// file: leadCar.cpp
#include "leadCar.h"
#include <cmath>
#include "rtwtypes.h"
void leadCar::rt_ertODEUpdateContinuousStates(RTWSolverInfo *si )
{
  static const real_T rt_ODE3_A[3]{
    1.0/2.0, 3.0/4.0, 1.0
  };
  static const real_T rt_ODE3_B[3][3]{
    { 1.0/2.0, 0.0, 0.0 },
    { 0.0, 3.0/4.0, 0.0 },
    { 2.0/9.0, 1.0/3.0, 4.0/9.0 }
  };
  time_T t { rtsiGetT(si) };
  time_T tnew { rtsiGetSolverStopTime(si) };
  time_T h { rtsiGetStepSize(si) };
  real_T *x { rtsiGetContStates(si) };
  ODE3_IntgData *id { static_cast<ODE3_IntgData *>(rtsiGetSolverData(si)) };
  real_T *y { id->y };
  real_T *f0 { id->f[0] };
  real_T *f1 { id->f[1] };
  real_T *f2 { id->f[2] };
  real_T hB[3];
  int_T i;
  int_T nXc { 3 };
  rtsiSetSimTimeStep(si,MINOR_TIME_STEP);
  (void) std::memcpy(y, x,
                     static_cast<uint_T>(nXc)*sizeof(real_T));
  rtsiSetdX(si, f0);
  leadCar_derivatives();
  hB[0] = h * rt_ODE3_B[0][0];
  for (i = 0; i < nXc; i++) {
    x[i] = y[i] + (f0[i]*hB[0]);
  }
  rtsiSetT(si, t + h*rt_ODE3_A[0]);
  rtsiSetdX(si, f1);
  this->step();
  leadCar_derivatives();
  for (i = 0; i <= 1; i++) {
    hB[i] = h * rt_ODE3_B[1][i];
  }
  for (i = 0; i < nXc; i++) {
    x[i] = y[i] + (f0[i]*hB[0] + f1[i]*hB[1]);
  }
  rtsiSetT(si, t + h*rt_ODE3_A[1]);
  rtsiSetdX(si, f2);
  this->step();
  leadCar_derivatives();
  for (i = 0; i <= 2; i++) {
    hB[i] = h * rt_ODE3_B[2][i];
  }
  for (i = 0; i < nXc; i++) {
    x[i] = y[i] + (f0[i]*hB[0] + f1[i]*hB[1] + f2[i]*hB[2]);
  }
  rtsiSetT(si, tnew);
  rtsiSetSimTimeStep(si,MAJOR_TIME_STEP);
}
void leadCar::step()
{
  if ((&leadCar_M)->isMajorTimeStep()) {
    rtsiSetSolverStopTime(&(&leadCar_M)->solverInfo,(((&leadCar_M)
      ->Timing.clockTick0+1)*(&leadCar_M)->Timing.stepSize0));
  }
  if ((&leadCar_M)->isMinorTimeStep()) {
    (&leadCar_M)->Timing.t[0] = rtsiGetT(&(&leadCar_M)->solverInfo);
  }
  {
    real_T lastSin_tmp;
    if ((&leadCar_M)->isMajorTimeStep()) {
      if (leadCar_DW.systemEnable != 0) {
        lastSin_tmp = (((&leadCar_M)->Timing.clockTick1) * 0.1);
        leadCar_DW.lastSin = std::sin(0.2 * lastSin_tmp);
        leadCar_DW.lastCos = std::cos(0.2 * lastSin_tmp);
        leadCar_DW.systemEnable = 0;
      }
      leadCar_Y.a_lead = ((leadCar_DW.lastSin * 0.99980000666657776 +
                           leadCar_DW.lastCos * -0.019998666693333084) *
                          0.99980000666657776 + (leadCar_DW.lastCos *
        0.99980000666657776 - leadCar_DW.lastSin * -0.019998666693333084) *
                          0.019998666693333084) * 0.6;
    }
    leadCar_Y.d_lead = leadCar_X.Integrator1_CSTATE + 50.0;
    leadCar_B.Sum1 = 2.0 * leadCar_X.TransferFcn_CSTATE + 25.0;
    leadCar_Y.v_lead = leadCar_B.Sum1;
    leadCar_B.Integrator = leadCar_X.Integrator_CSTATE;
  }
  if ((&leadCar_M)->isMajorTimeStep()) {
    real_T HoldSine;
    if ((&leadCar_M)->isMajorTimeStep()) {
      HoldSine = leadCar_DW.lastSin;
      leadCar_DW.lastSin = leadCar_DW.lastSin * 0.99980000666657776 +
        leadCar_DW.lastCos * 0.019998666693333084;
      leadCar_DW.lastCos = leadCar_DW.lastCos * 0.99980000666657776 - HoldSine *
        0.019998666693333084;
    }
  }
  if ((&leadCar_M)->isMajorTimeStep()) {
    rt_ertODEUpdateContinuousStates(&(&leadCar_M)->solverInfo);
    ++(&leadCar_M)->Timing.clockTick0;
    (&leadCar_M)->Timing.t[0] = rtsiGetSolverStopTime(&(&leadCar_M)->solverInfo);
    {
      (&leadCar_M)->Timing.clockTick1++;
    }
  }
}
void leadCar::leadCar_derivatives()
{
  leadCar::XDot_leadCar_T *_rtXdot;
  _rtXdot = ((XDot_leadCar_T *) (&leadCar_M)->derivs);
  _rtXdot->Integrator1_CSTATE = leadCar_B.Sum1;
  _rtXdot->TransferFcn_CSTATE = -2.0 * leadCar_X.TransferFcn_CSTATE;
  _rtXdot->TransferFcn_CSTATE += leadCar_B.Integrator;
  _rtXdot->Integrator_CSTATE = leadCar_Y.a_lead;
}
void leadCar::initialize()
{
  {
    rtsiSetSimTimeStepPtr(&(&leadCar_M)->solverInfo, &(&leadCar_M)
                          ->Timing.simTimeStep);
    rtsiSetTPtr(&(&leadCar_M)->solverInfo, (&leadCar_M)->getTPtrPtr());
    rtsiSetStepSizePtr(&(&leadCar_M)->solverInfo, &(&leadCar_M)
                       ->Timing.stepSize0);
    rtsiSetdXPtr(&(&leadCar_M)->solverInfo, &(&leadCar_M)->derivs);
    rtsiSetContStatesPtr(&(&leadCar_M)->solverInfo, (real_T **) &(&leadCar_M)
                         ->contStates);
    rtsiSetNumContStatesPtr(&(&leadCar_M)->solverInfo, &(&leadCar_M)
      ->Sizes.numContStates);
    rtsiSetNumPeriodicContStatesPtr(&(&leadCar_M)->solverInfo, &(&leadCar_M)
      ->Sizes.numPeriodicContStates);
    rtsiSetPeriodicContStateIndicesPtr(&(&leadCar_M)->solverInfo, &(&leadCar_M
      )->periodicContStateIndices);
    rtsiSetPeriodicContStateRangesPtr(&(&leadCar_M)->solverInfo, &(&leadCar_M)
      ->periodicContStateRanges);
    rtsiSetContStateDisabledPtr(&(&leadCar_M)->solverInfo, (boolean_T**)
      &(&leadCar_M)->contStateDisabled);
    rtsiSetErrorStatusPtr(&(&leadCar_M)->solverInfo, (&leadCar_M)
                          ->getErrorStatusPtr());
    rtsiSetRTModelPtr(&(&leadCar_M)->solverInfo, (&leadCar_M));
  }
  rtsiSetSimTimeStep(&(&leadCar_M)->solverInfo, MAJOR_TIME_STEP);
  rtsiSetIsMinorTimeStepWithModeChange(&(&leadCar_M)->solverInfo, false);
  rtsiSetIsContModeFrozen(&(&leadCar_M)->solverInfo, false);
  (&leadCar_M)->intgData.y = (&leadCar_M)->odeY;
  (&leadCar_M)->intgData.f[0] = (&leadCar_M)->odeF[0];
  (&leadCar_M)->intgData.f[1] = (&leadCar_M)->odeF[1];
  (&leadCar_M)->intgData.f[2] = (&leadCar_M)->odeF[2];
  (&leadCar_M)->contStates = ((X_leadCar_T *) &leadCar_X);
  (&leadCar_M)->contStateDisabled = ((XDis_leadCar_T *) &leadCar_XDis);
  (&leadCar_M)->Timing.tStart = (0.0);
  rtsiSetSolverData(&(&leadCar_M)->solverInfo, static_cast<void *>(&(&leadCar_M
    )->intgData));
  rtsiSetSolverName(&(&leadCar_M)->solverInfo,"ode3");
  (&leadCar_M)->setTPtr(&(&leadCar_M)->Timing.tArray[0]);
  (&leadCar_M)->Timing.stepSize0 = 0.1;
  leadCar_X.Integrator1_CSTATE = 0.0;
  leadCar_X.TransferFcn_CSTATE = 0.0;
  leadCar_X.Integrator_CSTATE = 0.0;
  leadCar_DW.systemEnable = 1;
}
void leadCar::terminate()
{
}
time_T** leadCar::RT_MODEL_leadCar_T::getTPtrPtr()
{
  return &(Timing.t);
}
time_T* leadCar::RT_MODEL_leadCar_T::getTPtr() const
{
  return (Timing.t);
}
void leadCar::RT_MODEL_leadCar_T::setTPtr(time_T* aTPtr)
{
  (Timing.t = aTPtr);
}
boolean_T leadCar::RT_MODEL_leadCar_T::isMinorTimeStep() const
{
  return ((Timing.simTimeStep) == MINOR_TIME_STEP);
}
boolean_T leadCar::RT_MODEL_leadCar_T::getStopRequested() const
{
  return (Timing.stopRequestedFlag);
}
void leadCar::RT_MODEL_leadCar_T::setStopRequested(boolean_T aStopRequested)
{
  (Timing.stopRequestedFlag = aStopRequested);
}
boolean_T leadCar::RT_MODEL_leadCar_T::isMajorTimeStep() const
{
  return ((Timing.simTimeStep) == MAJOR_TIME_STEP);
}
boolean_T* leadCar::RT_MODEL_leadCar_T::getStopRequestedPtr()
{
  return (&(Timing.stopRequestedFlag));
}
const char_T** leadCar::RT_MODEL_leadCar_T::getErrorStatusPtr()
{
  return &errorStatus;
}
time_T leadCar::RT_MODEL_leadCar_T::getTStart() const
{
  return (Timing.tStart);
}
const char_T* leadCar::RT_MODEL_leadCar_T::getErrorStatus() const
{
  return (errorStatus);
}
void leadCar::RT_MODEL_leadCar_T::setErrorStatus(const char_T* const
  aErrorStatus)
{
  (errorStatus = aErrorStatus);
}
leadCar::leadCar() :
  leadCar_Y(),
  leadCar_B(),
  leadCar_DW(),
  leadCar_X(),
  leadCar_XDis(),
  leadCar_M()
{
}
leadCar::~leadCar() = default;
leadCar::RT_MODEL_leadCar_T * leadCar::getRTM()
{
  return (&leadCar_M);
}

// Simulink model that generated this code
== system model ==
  a_lead : Outport  <- 1: Sin#1
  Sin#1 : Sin  Amplitude=0.6  Frequency=0.2
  d_lead : Outport  <- 1: Sum#1
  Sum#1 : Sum  <- 1: Constant#1, 2: Integrator1
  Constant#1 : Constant  Value=50
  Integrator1 : Integrator  <- 1: Sum1
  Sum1 : Sum  <- 1: TransferFcn, 2: Constant#2
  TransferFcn : TransferFcn  Denominator=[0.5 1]  <- 1: Integrator
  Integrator : Integrator  <- 1: Sin#1
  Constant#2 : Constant  Value=25
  v_lead : Outport  <- 1: Sum1
